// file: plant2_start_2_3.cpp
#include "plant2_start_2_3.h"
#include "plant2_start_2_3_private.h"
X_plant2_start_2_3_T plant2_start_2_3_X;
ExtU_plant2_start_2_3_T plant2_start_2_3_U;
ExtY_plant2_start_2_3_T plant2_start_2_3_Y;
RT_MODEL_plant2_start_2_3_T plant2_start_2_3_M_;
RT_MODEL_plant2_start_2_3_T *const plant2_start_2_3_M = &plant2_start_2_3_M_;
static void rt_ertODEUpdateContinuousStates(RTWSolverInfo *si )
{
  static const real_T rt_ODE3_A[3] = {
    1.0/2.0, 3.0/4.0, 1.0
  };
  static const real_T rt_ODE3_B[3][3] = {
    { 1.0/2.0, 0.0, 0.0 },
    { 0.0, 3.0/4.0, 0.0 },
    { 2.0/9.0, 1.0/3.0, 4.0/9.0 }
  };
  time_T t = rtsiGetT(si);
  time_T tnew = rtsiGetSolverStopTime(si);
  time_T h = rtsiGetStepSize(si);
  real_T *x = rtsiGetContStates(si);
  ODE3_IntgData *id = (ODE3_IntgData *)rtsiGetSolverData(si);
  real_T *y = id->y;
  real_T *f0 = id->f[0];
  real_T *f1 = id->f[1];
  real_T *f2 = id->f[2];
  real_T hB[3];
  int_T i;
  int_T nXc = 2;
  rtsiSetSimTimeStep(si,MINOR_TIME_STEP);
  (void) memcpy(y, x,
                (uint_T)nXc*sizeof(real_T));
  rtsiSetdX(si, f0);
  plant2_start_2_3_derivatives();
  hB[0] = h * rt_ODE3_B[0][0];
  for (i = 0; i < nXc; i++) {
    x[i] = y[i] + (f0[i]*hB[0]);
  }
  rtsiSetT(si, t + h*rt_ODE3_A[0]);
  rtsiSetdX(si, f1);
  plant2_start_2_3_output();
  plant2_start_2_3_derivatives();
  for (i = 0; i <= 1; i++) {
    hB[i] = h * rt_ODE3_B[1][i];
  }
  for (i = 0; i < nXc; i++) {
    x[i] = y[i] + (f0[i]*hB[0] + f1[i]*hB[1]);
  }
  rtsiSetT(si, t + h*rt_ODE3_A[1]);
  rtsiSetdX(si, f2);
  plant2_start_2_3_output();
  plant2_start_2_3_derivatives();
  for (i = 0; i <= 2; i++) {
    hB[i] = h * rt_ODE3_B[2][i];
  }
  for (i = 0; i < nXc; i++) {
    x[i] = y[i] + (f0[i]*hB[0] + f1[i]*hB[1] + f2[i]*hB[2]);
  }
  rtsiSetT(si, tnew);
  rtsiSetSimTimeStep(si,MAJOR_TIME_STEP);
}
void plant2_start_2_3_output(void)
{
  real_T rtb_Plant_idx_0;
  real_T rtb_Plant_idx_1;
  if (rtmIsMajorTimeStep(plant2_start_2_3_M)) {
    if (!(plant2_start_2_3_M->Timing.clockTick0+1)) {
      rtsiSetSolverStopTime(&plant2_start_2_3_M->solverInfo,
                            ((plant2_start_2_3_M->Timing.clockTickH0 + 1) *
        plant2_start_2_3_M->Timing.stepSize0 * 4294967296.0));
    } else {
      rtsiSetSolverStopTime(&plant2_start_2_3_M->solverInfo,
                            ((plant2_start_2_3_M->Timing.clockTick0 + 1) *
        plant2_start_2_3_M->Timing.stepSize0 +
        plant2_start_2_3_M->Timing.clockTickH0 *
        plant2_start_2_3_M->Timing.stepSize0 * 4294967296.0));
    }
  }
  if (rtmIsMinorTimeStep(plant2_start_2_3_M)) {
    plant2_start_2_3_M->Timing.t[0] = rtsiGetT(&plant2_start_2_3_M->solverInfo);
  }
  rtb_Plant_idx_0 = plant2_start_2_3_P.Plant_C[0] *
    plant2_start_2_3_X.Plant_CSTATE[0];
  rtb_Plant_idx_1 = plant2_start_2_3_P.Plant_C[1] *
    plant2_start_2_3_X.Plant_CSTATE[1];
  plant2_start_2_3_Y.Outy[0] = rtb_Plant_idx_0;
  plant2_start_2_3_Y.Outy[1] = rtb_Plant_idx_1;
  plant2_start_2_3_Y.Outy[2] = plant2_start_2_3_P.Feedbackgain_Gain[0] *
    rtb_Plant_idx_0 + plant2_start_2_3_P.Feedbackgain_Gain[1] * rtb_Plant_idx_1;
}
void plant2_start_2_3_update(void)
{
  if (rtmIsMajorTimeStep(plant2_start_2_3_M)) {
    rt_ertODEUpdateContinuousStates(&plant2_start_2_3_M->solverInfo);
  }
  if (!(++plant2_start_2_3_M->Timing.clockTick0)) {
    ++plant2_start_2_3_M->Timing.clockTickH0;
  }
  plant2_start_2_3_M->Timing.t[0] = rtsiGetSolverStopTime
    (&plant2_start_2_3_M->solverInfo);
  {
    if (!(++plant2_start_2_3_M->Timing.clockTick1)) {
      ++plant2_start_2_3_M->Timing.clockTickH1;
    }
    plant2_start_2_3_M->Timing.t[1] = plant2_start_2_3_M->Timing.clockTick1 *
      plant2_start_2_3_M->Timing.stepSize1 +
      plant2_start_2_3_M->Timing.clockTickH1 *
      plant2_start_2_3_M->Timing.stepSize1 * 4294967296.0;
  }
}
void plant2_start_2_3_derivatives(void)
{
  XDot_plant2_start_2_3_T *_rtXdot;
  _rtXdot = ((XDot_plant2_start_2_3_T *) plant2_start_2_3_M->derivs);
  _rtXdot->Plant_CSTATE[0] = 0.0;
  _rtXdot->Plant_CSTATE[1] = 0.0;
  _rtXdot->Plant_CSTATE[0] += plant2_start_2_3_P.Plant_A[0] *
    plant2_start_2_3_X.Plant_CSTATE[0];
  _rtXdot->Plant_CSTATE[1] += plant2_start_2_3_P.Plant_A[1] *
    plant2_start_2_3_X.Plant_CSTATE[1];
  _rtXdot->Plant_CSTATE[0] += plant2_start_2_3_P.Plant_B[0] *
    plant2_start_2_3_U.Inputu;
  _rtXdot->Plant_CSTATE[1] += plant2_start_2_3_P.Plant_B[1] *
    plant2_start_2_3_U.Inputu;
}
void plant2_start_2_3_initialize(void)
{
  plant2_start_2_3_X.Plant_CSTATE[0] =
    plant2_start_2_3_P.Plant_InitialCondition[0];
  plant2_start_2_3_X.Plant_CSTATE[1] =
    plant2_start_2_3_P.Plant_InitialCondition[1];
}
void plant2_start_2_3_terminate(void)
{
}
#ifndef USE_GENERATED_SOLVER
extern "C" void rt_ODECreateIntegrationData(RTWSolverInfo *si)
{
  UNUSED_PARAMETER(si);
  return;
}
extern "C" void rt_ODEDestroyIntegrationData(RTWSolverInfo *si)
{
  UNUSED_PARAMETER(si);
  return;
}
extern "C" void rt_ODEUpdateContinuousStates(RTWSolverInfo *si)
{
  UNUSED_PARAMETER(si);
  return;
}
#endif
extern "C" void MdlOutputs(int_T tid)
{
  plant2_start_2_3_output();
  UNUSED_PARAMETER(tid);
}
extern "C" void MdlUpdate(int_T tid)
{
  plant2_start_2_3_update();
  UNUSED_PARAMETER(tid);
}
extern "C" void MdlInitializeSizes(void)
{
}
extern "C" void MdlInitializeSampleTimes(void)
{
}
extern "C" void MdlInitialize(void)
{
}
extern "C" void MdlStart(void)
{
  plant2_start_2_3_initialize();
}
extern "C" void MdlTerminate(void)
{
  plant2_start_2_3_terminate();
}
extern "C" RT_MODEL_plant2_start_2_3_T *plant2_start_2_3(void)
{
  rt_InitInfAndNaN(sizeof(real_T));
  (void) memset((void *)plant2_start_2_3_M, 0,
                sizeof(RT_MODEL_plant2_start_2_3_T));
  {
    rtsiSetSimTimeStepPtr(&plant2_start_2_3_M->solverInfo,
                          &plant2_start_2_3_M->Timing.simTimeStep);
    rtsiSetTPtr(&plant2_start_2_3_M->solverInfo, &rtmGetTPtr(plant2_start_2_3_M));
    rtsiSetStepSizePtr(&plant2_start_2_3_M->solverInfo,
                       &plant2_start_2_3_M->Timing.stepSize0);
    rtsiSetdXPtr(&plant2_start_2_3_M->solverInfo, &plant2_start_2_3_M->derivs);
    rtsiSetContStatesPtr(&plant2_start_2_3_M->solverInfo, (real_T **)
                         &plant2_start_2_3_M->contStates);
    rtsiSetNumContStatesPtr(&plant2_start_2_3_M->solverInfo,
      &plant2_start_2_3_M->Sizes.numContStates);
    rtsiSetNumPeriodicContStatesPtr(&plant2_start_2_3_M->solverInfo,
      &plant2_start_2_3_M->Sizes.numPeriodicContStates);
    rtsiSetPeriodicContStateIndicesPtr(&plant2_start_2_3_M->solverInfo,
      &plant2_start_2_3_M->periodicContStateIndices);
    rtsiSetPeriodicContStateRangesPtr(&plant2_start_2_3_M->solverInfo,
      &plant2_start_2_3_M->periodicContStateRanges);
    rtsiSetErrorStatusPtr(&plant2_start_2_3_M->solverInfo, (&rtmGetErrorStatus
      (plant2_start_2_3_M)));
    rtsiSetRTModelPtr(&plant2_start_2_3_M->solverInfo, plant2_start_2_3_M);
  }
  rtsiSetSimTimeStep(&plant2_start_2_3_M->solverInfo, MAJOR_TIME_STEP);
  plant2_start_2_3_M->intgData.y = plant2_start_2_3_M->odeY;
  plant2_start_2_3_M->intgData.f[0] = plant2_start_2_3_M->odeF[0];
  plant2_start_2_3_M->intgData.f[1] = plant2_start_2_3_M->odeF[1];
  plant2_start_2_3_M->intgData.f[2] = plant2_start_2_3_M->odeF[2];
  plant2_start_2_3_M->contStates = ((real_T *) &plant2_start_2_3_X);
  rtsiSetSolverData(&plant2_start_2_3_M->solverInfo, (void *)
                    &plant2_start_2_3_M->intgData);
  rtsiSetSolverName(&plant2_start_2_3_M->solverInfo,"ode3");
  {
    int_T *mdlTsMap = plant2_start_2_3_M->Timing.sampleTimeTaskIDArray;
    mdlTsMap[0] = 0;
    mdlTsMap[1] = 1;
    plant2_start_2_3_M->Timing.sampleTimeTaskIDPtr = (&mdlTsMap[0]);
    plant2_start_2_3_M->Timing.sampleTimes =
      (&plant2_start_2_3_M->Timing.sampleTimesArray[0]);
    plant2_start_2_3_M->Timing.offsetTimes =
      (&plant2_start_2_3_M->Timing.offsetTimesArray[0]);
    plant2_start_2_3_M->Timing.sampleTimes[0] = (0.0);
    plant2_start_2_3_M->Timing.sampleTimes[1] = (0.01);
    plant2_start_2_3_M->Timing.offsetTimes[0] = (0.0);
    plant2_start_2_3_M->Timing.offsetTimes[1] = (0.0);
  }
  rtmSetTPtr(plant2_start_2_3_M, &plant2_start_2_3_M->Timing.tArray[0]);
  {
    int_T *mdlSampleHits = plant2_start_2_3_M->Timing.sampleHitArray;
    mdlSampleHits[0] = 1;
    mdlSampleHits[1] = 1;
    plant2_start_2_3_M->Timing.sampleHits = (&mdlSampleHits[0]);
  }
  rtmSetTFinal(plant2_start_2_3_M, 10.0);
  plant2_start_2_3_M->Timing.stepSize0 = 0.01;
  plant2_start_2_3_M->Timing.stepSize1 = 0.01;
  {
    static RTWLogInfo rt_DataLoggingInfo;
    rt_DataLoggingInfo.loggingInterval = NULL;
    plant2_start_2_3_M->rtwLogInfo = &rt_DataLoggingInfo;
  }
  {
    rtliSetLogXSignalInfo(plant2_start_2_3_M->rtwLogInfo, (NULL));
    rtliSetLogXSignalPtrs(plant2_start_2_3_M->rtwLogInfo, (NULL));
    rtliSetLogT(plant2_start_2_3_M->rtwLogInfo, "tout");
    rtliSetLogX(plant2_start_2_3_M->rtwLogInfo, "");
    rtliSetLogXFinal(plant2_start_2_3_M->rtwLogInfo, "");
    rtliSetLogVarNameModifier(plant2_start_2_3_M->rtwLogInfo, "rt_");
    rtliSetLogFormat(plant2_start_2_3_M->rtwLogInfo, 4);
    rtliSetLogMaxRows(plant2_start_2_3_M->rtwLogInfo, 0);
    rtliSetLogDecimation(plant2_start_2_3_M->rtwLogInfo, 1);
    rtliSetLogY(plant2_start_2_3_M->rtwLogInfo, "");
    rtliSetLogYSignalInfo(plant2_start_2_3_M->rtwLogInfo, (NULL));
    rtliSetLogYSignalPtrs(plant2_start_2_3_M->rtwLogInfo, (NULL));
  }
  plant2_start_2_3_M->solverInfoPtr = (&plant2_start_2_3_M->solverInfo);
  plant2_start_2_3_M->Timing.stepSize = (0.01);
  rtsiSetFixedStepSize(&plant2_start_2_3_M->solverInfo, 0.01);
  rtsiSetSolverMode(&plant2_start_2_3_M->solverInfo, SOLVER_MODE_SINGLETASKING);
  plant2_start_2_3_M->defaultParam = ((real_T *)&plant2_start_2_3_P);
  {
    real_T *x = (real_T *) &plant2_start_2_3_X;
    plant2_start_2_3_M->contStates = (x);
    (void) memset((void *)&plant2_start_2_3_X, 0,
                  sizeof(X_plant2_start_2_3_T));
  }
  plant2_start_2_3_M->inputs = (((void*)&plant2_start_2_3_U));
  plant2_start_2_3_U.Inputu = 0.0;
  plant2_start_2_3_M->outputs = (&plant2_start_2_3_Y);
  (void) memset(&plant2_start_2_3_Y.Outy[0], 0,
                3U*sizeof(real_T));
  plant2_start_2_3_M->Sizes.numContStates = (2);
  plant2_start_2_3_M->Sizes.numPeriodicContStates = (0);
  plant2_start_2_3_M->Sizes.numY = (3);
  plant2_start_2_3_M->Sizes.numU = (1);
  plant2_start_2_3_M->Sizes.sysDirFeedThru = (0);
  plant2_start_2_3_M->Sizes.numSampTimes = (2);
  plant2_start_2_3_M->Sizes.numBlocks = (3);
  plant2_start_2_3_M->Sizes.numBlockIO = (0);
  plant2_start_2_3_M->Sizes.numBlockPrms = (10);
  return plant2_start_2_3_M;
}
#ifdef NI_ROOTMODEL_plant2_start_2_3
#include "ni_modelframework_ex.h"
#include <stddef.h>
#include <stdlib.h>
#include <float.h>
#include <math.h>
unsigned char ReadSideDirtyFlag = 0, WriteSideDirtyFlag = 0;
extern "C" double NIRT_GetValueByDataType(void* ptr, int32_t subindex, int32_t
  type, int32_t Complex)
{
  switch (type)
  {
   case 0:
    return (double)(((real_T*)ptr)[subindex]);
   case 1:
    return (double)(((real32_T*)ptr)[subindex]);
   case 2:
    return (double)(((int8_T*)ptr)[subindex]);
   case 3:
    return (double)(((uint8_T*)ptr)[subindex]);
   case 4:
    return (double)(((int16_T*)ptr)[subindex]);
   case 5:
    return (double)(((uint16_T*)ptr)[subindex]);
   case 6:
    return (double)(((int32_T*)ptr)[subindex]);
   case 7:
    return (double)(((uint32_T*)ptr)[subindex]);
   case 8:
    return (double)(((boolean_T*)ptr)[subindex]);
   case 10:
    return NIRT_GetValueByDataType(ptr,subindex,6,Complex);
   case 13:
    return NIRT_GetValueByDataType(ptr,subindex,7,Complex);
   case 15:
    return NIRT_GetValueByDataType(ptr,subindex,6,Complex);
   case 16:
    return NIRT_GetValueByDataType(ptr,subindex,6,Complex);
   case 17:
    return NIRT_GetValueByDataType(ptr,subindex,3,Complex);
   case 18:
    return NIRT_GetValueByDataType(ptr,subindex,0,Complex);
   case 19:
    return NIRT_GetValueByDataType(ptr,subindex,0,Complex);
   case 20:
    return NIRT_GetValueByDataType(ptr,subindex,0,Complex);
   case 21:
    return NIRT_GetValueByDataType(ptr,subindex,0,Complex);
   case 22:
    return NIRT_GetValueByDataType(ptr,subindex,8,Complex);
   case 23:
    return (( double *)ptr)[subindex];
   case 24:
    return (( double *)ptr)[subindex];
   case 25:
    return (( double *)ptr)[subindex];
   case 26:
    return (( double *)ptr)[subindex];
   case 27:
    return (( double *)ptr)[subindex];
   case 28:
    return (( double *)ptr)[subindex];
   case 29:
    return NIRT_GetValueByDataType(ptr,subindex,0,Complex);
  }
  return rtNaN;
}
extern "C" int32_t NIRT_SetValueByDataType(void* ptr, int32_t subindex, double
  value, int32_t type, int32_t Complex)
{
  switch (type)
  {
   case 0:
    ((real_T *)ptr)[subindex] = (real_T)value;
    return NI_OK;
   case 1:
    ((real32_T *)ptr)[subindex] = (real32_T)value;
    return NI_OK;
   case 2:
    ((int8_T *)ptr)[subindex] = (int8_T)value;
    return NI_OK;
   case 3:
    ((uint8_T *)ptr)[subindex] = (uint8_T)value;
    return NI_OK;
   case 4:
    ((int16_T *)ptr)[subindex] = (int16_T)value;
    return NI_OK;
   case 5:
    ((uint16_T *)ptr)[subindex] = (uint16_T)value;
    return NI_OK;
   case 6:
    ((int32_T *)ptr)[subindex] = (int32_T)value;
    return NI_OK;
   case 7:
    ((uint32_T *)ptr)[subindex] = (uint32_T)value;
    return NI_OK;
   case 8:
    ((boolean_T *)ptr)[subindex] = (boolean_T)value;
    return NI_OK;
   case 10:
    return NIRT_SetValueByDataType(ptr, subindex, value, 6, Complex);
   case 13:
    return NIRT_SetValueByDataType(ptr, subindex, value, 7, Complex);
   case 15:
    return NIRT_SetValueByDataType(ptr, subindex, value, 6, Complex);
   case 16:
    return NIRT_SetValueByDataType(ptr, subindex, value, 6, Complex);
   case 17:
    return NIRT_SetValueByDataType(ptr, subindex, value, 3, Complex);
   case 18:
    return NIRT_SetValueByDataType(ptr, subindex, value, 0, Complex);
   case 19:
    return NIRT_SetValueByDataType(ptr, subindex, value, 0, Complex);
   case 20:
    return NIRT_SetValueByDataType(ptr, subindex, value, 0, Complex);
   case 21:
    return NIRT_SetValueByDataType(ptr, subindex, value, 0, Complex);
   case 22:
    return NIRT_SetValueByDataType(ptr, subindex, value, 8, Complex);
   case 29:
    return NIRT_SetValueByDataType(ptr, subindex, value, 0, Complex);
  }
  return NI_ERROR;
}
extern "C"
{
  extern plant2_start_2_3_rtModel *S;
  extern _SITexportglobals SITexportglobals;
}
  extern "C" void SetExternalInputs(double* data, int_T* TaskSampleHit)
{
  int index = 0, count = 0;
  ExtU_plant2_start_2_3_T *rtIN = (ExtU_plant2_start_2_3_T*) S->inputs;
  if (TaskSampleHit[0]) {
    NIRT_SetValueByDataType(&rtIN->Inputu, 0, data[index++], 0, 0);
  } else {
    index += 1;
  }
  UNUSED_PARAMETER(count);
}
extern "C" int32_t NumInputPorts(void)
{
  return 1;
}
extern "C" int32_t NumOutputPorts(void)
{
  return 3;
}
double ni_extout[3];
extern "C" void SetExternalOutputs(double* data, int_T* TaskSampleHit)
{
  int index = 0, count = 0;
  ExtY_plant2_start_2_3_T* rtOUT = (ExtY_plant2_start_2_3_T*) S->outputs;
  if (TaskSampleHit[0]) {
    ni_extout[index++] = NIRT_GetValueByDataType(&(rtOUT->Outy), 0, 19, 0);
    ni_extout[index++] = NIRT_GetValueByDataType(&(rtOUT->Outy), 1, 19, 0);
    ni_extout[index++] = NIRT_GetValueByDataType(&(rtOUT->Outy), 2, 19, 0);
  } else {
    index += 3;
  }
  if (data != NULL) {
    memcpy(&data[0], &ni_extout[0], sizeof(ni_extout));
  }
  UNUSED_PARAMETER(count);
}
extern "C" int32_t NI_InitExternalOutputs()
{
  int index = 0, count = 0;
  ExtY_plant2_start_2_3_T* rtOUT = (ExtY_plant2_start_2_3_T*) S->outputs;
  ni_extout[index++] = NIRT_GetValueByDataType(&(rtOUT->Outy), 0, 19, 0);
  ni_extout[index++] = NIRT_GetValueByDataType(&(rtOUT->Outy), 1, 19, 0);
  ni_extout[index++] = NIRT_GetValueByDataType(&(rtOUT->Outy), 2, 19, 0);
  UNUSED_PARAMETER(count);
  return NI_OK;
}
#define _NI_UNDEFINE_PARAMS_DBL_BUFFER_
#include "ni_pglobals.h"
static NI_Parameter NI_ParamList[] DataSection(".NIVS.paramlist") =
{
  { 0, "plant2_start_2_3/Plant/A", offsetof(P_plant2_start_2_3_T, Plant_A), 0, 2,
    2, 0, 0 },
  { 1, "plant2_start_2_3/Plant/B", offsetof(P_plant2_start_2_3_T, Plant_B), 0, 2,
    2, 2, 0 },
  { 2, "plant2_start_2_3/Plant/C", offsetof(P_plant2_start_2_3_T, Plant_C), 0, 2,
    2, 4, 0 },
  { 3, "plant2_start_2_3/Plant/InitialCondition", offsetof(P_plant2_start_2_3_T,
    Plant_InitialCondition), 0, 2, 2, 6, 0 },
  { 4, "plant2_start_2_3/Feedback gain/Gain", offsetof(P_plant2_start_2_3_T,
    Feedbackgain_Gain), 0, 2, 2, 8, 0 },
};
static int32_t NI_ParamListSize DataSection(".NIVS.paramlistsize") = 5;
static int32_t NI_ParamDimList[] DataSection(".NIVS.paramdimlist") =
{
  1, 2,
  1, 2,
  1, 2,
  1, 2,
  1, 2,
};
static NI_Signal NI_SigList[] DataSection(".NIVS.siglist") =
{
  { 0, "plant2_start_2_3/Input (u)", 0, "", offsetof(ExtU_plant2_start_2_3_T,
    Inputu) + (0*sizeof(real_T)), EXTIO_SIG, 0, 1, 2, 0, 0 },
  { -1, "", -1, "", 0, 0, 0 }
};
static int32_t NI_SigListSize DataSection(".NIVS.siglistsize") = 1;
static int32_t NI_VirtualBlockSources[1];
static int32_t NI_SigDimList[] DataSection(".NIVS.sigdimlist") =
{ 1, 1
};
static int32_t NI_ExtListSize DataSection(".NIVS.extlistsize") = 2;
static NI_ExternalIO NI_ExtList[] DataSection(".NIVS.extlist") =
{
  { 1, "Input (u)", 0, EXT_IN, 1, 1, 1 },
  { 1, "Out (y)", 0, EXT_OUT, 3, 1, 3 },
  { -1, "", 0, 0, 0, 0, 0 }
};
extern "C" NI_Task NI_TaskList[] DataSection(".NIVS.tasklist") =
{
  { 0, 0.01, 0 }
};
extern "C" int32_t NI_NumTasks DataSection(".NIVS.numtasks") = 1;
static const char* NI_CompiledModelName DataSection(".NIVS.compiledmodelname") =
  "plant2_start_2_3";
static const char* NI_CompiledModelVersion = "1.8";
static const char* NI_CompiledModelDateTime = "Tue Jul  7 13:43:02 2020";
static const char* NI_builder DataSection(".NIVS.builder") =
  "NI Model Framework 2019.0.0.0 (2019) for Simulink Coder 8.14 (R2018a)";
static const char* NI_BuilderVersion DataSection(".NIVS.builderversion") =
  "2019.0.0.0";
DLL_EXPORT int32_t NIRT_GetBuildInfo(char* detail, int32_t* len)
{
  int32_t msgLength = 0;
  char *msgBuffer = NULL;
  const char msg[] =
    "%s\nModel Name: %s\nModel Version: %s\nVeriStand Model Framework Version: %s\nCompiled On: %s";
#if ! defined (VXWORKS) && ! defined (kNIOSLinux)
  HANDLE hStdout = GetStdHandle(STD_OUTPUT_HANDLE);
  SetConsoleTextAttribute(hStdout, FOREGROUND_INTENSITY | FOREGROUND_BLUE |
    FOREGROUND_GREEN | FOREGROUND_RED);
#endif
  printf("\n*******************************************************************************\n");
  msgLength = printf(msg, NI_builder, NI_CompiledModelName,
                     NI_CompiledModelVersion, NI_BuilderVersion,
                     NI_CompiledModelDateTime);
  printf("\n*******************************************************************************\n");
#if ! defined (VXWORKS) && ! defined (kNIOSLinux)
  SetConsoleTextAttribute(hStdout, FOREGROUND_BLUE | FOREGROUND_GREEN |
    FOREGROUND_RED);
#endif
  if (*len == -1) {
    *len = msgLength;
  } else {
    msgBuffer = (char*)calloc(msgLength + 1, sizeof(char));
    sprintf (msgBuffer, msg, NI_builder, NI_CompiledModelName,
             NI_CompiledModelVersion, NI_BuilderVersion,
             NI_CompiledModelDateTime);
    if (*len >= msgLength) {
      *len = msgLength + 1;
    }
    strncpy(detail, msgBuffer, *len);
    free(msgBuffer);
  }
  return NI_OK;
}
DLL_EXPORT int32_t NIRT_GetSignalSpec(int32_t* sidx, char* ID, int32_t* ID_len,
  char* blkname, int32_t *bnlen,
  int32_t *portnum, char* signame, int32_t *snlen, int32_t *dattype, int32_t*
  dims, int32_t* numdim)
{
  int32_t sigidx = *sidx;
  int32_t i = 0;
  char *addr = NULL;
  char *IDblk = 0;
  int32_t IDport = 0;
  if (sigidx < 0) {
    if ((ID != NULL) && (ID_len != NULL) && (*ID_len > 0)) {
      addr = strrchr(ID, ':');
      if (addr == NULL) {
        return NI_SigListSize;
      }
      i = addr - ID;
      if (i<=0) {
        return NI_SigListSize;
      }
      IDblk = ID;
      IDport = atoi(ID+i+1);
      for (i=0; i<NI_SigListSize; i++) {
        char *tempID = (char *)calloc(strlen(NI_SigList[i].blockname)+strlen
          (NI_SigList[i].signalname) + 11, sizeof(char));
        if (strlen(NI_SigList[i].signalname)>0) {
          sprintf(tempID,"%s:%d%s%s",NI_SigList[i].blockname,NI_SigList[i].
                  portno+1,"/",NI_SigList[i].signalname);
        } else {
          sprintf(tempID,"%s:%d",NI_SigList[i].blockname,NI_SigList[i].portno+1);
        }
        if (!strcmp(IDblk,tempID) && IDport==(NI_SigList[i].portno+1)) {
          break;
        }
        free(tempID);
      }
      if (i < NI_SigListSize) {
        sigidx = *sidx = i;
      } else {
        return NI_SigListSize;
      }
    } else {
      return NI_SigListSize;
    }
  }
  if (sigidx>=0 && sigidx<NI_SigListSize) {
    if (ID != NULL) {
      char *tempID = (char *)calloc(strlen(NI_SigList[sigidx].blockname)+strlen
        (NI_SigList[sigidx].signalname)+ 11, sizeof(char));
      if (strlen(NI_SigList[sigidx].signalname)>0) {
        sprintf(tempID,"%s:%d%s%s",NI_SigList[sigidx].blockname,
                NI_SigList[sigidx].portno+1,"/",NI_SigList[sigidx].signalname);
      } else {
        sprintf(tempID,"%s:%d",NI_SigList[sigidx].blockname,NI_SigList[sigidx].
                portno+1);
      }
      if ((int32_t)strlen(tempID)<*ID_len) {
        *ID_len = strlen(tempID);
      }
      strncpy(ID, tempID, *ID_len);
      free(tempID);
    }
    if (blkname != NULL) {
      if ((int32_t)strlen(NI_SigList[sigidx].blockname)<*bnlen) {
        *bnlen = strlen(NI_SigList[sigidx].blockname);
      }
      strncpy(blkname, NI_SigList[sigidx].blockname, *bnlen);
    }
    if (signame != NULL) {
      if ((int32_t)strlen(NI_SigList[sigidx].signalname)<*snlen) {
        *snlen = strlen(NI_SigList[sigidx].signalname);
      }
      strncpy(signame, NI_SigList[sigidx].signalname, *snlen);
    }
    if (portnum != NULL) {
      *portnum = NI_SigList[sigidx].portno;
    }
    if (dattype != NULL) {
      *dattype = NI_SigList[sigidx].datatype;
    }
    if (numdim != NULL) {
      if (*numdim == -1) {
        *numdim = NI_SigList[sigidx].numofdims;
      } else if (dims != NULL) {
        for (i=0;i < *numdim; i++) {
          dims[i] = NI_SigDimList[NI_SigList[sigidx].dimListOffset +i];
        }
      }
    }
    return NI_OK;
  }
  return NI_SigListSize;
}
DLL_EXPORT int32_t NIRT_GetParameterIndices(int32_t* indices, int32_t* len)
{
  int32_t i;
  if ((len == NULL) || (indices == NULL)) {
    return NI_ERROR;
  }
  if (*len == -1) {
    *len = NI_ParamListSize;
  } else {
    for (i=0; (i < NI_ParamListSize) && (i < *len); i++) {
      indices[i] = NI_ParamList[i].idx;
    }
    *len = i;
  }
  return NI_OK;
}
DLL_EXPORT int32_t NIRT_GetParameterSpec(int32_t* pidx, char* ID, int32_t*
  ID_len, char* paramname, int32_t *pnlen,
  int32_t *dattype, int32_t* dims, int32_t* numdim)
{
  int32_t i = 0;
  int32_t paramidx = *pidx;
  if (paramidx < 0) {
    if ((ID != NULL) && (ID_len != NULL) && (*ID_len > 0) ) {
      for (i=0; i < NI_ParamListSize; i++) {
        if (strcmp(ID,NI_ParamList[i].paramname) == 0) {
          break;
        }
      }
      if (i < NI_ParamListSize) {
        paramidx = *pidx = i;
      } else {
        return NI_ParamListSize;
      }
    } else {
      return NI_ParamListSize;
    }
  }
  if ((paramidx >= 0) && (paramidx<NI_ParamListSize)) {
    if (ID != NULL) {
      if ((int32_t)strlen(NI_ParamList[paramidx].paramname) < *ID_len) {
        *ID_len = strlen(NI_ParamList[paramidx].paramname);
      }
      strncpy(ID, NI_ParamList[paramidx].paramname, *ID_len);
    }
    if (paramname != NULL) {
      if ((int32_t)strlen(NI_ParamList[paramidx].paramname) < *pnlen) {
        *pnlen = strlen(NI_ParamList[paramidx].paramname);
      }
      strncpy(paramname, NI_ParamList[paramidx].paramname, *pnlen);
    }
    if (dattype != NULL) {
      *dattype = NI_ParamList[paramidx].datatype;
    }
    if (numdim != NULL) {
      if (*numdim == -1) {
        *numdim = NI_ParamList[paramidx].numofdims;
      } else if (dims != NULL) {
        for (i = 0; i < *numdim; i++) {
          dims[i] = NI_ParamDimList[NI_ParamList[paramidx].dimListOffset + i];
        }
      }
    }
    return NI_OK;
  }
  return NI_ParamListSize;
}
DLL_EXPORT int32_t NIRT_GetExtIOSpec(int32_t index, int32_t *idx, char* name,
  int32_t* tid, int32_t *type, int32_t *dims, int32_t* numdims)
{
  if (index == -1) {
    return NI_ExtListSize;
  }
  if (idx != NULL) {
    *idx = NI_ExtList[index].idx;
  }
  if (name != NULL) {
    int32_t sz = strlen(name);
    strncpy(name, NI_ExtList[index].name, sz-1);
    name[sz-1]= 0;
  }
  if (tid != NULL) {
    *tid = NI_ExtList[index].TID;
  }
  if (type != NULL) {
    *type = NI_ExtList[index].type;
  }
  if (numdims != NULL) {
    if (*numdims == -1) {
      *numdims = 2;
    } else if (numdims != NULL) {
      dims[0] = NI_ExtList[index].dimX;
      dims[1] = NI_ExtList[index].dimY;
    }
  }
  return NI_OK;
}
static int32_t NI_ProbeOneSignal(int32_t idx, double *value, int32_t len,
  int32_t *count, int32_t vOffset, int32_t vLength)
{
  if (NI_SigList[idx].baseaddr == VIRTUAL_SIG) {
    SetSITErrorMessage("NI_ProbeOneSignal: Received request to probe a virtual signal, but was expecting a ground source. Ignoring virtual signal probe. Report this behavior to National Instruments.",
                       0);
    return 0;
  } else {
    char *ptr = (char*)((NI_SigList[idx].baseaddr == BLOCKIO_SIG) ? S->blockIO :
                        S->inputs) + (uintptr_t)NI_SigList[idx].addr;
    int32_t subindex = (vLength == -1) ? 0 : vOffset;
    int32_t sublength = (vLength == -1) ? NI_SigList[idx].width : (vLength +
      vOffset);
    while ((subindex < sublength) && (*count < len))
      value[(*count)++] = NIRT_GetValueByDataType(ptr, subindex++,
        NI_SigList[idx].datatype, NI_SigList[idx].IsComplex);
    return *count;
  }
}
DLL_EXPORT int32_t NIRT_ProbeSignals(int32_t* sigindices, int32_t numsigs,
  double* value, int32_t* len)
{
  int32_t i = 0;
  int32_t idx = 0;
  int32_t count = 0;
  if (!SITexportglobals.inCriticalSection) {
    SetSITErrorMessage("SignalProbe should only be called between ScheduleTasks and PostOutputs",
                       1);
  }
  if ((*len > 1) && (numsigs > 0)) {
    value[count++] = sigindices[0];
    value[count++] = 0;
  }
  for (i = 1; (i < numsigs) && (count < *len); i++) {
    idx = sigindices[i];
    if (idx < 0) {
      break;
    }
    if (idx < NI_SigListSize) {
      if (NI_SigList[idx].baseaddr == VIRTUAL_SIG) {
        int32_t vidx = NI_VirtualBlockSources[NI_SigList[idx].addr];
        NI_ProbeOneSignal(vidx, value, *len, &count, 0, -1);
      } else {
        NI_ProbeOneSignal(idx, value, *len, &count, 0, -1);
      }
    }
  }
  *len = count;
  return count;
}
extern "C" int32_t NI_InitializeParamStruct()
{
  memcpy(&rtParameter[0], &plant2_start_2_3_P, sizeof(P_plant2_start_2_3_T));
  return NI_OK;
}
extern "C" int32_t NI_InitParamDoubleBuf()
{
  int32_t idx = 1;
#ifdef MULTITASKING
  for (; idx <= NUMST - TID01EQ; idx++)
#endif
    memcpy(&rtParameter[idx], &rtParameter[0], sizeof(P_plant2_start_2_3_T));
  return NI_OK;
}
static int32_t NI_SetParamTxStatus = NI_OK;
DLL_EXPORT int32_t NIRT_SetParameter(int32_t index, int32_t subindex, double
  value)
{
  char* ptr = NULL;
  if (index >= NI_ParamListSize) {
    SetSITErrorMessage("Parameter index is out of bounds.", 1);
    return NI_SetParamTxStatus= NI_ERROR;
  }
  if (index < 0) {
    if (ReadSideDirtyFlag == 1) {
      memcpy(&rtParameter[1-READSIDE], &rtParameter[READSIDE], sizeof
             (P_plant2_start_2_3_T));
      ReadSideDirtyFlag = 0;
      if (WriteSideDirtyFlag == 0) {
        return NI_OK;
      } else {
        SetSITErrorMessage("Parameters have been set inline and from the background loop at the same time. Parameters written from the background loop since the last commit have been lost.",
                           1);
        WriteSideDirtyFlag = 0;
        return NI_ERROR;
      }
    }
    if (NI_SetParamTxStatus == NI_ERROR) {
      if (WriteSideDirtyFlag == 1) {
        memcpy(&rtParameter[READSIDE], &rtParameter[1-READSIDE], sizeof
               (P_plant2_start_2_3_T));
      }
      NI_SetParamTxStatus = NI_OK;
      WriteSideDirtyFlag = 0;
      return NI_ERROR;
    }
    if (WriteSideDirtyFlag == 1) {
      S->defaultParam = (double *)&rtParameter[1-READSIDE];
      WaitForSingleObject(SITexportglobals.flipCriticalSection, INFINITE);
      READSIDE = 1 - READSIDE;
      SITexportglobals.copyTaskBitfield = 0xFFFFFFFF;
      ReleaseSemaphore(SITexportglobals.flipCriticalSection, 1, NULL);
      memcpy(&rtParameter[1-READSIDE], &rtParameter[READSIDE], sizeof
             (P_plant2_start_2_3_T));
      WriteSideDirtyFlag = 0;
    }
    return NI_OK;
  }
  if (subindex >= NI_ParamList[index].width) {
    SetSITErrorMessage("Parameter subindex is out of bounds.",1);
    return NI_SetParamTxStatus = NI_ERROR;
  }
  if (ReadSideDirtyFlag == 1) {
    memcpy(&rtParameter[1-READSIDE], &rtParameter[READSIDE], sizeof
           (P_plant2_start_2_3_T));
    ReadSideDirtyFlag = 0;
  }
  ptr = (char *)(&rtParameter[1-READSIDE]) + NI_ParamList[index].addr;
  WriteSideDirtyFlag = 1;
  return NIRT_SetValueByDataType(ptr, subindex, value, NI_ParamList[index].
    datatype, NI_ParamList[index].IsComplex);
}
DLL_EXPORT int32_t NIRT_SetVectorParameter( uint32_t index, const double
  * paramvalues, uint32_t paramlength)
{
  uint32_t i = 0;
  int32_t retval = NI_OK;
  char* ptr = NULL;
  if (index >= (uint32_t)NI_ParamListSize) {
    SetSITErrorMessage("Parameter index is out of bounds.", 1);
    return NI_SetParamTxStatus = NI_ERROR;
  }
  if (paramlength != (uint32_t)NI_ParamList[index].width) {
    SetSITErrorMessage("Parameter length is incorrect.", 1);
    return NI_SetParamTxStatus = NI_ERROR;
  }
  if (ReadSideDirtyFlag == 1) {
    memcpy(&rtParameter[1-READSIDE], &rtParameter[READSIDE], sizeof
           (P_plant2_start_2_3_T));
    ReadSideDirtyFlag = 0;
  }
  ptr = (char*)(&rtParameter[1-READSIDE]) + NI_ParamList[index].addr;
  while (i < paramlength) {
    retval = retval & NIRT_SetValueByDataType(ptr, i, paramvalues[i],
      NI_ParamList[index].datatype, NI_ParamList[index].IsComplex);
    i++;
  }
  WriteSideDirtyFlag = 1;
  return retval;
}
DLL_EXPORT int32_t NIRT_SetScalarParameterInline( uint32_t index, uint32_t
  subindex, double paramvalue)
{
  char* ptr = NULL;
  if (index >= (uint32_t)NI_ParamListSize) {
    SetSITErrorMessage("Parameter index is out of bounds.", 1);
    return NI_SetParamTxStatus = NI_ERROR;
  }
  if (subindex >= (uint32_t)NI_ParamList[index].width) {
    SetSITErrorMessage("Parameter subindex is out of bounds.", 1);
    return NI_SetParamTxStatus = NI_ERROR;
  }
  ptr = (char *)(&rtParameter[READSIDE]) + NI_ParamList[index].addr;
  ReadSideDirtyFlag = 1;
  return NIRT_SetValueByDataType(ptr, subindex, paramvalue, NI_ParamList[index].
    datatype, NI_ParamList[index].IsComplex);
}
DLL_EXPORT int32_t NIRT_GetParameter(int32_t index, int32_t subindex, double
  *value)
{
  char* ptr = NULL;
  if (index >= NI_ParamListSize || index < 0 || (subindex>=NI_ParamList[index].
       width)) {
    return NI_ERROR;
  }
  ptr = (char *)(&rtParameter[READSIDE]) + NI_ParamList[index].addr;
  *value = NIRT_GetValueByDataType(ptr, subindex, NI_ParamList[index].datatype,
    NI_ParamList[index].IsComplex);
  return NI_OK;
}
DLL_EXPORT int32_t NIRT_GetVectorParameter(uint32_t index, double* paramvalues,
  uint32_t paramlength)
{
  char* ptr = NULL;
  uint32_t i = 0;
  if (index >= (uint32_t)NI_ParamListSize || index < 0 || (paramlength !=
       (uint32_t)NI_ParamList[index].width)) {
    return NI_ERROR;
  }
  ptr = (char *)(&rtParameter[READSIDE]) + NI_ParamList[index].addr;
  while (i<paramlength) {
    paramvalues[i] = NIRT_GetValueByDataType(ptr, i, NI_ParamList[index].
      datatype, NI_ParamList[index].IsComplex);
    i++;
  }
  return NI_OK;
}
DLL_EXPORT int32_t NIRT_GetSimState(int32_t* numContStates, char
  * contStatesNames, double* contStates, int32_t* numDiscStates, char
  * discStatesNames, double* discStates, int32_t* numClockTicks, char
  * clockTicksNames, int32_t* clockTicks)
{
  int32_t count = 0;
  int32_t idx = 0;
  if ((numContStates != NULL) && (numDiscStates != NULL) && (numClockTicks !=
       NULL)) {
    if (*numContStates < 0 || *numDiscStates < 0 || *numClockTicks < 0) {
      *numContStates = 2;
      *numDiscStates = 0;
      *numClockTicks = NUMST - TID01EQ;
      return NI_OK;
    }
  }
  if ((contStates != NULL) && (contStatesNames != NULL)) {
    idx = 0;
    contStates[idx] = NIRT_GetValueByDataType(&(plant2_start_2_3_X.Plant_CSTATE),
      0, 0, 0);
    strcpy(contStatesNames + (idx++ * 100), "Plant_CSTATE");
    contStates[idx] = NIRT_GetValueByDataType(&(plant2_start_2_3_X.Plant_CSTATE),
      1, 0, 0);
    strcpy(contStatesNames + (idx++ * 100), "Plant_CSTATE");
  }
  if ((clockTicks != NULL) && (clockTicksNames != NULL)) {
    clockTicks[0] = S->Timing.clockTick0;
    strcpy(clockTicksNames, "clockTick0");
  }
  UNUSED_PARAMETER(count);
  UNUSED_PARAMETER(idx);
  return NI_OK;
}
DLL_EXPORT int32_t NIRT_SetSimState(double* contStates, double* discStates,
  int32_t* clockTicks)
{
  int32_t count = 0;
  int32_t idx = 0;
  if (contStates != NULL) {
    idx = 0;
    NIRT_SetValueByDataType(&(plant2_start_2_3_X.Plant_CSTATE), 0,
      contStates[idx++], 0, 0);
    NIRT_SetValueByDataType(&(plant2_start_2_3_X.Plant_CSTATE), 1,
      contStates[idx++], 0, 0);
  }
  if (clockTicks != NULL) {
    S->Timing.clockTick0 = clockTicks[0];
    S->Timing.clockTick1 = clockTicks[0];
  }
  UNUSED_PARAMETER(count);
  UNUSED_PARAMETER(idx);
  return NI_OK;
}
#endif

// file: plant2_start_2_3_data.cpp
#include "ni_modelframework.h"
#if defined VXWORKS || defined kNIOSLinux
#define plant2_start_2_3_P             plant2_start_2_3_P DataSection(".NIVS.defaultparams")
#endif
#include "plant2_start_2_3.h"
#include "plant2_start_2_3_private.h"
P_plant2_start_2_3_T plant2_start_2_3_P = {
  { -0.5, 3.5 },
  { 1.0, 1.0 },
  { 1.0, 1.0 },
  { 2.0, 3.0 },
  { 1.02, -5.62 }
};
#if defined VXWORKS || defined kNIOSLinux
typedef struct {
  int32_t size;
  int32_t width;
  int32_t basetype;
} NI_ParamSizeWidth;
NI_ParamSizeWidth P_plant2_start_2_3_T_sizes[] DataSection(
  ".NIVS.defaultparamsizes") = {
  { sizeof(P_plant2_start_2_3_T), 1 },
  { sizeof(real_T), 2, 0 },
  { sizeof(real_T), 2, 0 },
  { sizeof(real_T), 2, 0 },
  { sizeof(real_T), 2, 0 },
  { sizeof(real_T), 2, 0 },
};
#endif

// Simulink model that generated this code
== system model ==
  Inputu : Inport
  Outy : Outport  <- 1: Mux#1
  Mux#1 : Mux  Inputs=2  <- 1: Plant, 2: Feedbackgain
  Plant : StateSpace  A=[-0.5 0; 0 3.5]  B=[1; 1]  C=[1 0; 0 1]  D=[0; 0]  InitialCondition=[2 3]  <- 1: Inputu
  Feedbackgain : Gain  Gain=[1.02 -5.62]  Multiplication=Matrix(K*u)  <- 1: Plant
